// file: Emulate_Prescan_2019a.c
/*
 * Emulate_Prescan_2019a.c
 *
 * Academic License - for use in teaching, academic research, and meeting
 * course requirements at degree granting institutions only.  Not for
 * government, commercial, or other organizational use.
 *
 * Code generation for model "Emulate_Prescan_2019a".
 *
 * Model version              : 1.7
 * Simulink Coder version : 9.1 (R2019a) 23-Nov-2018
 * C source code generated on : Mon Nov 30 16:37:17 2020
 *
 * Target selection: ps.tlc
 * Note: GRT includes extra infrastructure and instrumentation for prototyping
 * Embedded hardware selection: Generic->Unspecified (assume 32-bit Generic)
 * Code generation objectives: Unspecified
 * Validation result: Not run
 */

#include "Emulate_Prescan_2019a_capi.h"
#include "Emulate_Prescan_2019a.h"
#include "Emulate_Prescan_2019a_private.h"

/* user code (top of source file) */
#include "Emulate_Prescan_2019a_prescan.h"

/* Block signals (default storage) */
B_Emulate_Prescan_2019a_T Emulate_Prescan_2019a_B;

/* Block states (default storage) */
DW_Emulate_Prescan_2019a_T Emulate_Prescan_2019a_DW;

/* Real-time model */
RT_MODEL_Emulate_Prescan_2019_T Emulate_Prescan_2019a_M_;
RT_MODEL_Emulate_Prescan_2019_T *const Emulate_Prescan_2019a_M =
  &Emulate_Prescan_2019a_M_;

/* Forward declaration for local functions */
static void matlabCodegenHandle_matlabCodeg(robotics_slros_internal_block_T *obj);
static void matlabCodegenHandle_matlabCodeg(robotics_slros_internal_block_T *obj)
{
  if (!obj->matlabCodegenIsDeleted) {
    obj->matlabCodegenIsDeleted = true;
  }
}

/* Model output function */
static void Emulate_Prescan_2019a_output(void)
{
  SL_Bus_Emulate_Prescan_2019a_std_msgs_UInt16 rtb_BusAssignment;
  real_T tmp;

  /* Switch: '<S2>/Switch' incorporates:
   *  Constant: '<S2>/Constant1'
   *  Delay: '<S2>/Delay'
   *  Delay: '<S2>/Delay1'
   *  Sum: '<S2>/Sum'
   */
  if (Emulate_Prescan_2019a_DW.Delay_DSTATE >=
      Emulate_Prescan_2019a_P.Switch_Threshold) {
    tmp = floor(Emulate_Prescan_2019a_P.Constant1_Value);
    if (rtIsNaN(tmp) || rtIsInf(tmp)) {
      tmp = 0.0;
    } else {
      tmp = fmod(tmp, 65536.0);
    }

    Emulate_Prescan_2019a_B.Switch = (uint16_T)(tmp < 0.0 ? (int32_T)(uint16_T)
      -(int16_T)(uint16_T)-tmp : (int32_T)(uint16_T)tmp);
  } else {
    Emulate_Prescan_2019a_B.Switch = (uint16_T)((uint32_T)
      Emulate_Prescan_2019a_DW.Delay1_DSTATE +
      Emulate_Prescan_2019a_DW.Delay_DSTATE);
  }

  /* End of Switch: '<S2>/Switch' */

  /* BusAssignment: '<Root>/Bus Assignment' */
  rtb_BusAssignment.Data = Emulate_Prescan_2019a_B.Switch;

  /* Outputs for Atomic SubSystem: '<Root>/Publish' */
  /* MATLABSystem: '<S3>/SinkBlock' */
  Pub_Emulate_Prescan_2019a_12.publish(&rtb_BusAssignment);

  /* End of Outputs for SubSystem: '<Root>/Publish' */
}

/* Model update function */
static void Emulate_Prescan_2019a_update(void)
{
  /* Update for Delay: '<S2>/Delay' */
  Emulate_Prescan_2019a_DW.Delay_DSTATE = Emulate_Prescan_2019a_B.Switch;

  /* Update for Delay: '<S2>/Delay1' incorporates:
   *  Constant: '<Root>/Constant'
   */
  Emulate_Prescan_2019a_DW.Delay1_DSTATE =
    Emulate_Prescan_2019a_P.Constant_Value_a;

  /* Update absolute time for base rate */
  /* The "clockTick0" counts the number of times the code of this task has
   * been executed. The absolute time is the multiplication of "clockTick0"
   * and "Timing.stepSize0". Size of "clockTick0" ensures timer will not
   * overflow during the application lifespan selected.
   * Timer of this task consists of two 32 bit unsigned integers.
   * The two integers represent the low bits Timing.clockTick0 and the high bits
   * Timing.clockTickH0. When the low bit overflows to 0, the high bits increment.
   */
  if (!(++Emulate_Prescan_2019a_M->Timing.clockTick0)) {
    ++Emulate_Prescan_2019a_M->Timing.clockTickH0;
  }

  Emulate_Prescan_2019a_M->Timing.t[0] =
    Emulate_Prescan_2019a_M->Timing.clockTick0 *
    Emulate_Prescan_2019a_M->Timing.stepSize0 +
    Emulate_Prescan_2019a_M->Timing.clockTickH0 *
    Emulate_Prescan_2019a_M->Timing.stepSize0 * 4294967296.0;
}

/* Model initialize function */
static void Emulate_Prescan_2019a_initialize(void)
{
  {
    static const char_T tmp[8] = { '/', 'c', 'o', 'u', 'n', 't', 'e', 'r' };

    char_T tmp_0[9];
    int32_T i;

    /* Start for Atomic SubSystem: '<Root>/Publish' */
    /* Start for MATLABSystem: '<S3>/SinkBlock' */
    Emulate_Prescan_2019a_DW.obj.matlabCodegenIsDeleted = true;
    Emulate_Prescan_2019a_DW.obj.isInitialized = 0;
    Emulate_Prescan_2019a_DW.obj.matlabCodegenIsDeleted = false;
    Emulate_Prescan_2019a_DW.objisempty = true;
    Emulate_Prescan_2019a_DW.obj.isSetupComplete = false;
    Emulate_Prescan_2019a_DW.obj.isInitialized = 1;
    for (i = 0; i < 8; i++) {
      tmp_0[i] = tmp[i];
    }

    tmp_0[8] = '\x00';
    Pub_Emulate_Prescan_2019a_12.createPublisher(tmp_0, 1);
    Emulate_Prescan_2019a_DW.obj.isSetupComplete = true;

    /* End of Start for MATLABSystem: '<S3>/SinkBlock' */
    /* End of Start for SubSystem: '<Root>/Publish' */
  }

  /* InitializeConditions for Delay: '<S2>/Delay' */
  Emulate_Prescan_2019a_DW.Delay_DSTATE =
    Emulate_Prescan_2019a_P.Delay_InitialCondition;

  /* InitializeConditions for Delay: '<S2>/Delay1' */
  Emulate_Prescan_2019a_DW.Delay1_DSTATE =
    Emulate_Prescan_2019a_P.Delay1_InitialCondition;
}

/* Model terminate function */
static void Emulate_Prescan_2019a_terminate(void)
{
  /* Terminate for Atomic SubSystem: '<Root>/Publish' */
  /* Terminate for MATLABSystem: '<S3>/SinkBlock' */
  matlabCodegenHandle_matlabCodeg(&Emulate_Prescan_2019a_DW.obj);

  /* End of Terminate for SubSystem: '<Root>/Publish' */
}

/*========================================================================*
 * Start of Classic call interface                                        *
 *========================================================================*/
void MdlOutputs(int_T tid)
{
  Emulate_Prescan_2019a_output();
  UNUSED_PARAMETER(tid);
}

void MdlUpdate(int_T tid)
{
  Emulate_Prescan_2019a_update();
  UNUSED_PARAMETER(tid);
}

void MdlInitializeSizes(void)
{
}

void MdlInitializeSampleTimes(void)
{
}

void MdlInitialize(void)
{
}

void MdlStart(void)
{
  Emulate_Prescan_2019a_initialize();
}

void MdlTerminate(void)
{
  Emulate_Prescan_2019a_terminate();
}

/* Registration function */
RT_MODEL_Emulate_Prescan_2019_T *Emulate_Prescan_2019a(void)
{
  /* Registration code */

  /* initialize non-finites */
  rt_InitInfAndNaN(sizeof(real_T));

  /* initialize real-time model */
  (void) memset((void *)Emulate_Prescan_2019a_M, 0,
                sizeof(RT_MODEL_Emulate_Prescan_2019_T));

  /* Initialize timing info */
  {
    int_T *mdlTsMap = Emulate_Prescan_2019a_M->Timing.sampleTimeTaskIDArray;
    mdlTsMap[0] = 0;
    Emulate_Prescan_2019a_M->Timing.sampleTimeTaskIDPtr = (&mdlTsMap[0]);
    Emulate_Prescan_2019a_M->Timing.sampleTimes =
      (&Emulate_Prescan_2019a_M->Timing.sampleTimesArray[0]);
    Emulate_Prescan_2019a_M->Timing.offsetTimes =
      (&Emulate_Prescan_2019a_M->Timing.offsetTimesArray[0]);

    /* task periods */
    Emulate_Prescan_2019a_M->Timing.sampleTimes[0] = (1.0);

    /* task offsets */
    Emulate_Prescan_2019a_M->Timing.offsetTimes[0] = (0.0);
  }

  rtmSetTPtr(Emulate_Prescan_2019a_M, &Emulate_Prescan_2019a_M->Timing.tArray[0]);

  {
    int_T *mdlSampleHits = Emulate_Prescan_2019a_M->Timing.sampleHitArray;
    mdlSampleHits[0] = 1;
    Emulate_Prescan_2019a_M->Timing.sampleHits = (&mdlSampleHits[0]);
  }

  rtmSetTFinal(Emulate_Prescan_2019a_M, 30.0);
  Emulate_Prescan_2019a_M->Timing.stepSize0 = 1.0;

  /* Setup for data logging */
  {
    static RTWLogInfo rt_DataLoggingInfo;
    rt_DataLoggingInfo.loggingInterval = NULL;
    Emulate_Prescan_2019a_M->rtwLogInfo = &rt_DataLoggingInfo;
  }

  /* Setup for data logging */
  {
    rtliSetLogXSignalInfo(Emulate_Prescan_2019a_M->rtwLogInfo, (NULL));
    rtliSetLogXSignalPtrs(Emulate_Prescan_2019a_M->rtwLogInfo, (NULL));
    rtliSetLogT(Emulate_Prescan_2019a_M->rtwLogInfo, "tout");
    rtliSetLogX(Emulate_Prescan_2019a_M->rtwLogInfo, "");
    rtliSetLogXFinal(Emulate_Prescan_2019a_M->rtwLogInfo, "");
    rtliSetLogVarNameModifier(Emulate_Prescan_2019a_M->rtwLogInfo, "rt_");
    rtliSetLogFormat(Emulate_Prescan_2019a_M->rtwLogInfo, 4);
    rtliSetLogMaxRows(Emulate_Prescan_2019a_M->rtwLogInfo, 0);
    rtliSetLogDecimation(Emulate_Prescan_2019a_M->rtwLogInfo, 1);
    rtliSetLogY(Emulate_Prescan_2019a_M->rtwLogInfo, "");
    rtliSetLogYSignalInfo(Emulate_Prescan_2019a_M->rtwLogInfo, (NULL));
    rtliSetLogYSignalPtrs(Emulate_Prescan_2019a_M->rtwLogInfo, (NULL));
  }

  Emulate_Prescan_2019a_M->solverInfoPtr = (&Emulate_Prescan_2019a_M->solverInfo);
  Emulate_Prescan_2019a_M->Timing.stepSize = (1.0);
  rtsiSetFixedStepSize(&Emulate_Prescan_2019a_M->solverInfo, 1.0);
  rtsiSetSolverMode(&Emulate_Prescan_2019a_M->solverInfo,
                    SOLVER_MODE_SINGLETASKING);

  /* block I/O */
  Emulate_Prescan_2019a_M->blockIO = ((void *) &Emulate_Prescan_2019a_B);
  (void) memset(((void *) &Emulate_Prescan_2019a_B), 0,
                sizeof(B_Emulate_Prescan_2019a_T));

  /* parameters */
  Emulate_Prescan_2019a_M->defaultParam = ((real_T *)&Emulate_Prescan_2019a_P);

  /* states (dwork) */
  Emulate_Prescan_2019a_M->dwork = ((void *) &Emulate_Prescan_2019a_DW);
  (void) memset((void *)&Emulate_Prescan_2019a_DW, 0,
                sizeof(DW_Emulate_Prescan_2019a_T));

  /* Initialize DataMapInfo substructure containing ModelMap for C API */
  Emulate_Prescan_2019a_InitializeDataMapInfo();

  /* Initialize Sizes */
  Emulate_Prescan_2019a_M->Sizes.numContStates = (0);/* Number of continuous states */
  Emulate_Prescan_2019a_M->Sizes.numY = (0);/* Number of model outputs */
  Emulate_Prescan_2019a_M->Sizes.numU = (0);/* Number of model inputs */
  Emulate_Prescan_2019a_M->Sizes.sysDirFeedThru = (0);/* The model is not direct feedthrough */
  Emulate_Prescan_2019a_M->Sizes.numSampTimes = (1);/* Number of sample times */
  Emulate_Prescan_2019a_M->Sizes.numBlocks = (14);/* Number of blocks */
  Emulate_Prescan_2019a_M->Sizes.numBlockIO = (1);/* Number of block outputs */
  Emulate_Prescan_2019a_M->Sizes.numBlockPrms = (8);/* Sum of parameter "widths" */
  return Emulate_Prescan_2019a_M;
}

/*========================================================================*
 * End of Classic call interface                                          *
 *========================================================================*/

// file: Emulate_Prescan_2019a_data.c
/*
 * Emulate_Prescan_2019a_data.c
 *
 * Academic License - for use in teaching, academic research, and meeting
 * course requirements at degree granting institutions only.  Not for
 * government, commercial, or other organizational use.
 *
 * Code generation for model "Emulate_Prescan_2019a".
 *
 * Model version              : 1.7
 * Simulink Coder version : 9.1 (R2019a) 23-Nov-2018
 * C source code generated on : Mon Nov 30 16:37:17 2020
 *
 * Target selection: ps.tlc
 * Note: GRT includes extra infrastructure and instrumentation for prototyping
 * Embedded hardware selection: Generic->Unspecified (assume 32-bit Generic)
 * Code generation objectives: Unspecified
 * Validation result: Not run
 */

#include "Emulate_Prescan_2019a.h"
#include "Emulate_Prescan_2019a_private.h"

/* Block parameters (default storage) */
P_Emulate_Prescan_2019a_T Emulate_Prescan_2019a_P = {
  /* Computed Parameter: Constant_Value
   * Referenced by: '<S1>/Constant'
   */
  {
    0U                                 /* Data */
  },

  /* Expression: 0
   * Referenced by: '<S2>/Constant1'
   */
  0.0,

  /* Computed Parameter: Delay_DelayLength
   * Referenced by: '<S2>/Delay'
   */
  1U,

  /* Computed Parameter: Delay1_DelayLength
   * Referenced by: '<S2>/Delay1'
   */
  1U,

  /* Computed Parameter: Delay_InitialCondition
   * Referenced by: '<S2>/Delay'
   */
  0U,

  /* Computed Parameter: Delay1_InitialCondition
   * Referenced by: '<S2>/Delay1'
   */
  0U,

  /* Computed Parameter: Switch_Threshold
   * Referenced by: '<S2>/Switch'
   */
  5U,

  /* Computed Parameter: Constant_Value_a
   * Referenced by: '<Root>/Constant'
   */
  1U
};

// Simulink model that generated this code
simulink model "Emulate_Prescan_2019a"  (R2019a)
settings: Solver=FixedStepDiscrete  StartTime=0.0  StopTime=30  FixedStep=1  RelTol=1e-3
libraries: robotlib x2

== system Emulate_Prescan_2019a ==
  Blank Message : robotlib/Blank Message  messageClass=Message  entityType=std_msgs/UInt16  messageType=std_msgs/UInt16  SampleTime=inf
  Bus Assignment : BusAssignment  AssignedSignals=Data
  Constant : Constant  OutDataTypeStr=uint16
  Prescan : Subsystem
  Publish : robotlib/Publish  topicSource=Specify your own  topic=/counter  messageType=std_msgs/UInt16  messageQueueLength=1
  Scope : Scope
  wires:
  Constant/1 -> Prescan/1(In1)
  Prescan/1(Out1) -> Bus Assignment/2, Scope/1
  Blank Message/1 -> Bus Assignment/1
  Bus Assignment/1 -> Publish/1

== system Emulate_Prescan_2019a/Prescan ==
  In1 : Inport
  Constant1 : Constant  Value=0
  Delay : Delay  DelayLength=1
  Delay1 : Delay  DelayLength=1
  Sum : Sum
  Switch : Switch  Threshold=5
  Out1 : Outport
  wires:
  Delay/1 -> Switch/2, Sum/2
  Constant1/1 -> Switch/1
  Delay1/1 -> Sum/1
  In1/1 -> Delay1/1
  Switch/1 -> Out1/1, Delay/1
  Sum/1 -> Switch/3
